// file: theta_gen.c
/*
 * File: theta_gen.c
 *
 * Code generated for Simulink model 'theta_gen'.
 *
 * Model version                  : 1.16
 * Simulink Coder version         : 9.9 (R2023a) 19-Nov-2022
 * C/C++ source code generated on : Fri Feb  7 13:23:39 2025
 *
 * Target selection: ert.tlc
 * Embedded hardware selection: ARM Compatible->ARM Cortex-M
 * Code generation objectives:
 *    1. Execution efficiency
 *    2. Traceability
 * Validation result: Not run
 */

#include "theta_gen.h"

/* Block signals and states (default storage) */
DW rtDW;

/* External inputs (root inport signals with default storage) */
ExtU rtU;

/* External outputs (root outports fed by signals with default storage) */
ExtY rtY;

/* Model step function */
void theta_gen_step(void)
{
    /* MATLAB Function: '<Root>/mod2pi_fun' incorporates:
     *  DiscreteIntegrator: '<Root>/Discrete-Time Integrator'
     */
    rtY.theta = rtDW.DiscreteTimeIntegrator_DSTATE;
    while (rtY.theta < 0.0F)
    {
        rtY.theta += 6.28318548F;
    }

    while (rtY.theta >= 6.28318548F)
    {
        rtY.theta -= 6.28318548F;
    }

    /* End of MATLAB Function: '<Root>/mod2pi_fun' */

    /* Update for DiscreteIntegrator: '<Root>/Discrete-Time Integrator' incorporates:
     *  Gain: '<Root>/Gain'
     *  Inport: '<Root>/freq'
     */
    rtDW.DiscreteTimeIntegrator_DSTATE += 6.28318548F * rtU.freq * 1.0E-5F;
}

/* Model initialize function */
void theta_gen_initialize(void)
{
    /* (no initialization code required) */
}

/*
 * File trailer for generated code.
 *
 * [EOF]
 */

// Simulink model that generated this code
simulink model "theta_gen"  (R2023a)
settings: Solver=FixedStepDiscrete  StartTime=0.0  StopTime=10.0  FixedStep=1e-5  RelTol=1e-3
model workspace (MATLAB code in the model file):
  | cmdLim = Simulink.Parameter;
  | cmdLim.Value = 15;
  | cmdLim.Description = 'Limit for controlling the maximum surface command angle.';
  | cmdLim.Min = 0;
  | cmdLim.Max = 90;
  | cmdLim.DocUnits = 'deg';
  | 
  | dispGain = Simulink.Parameter;
  | dispGain.Value = 0.75;
  | dispGain.Description = 'Gain applied to the displacement error.';
  | dispGain.Min = 0;
  | dispGain.Max = [];
  | dispGain.DocUnits = 'deg/sec/deg';
  | 
  | dispLim = Simulink.Parameter;
  | dispLim.Value = 30;
  | dispLim.Description = 'Limit for controlling the maximum commanded angle.';
  | dispLim.Min = 0;
  | dispLim.Max = 180;
  | dispLim.DocUnits = 'deg';
  | 
  | intGain = Simulink.Parameter;
  | intGain.Value = 0.5;
  | intGain.Description = 'Gain applied to the integral error.';
  | intGain.Min = 0;
  | intGain.Max = [];
  | intGain.DocUnits = 'deg/sec/deg/sec';
  | 
  | intLim = Simulink.Parameter;
  | intLim.Value = 5;
  | intLim.Description = 'Limit for controlling the maximum commanded angle.';
  | intLim.Min = 0;
  | intLim.Max = 90;
  | intLim.DocUnits = 'deg';
  | 
  | rateGain = Simulink.Parameter;
  | rateGain.Value = 2;
  | rateGain.Description = 'Gain applied to the rate error.';
  | rateGain.Min = 0;
  | rateGain.Max = [];
  | rateGain.DocUnits = 'deg/deg/sec';
  | 
  | rateLim = Simulink.Parameter;
  | rateLim.Value = 6;
  | rateLim.Description = 'Limit for controlling the maximum commanded angle.';
  | rateLim.Min = 0;
  | rateLim.Max = 180;
  | rateLim.DocUnits = 'deg/sec';
  | 
  | hdgGain = Simulink.Parameter;
  | hdgGain.Value = 0.015;
undefined symbols (not defined in the file): DiscIntNeverNeededParam

== system theta_gen ==
  freq : Inport
  Data Type Conversion : DataTypeConversion  OutDataTypeStr=single  SaturateOnIntegerOverflow=off  RndMeth=Floor
  Discrete-Time Integrator : DiscreteIntegrator  SampleTime=10e-6  ICPrevOutput=DiscIntNeverNeededParam  ICPrevScaledInput=DiscIntNeverNeededParam
  Gain : Gain  Gain=2*pi
  mod2pi_fun : MATLAB Function  TreatAsAtomicUnit=on
  theta : Outport
  wires:
  Discrete-Time Integrator/1 -> mod2pi_fun/1(ang)
  Data Type Conversion/1 -> Gain/1
  Gain/1 -> Discrete-Time Integrator/1
  mod2pi_fun/1(n_ang) -> theta/1
  freq/1 -> Data Type Conversion/1

== matlab function theta_gen/mod2pi_fun ==
function n_ang = mod2pi(ang)
    % 将角度限制在0到2π范围内
    TWO_PI = single(2*pi);
    n_ang = single(ang);
    while n_ang < 0
        n_ang = n_ang + TWO_PI;
    end
    while n_ang >= TWO_PI
        n_ang = n_ang - TWO_PI;
    end
end
